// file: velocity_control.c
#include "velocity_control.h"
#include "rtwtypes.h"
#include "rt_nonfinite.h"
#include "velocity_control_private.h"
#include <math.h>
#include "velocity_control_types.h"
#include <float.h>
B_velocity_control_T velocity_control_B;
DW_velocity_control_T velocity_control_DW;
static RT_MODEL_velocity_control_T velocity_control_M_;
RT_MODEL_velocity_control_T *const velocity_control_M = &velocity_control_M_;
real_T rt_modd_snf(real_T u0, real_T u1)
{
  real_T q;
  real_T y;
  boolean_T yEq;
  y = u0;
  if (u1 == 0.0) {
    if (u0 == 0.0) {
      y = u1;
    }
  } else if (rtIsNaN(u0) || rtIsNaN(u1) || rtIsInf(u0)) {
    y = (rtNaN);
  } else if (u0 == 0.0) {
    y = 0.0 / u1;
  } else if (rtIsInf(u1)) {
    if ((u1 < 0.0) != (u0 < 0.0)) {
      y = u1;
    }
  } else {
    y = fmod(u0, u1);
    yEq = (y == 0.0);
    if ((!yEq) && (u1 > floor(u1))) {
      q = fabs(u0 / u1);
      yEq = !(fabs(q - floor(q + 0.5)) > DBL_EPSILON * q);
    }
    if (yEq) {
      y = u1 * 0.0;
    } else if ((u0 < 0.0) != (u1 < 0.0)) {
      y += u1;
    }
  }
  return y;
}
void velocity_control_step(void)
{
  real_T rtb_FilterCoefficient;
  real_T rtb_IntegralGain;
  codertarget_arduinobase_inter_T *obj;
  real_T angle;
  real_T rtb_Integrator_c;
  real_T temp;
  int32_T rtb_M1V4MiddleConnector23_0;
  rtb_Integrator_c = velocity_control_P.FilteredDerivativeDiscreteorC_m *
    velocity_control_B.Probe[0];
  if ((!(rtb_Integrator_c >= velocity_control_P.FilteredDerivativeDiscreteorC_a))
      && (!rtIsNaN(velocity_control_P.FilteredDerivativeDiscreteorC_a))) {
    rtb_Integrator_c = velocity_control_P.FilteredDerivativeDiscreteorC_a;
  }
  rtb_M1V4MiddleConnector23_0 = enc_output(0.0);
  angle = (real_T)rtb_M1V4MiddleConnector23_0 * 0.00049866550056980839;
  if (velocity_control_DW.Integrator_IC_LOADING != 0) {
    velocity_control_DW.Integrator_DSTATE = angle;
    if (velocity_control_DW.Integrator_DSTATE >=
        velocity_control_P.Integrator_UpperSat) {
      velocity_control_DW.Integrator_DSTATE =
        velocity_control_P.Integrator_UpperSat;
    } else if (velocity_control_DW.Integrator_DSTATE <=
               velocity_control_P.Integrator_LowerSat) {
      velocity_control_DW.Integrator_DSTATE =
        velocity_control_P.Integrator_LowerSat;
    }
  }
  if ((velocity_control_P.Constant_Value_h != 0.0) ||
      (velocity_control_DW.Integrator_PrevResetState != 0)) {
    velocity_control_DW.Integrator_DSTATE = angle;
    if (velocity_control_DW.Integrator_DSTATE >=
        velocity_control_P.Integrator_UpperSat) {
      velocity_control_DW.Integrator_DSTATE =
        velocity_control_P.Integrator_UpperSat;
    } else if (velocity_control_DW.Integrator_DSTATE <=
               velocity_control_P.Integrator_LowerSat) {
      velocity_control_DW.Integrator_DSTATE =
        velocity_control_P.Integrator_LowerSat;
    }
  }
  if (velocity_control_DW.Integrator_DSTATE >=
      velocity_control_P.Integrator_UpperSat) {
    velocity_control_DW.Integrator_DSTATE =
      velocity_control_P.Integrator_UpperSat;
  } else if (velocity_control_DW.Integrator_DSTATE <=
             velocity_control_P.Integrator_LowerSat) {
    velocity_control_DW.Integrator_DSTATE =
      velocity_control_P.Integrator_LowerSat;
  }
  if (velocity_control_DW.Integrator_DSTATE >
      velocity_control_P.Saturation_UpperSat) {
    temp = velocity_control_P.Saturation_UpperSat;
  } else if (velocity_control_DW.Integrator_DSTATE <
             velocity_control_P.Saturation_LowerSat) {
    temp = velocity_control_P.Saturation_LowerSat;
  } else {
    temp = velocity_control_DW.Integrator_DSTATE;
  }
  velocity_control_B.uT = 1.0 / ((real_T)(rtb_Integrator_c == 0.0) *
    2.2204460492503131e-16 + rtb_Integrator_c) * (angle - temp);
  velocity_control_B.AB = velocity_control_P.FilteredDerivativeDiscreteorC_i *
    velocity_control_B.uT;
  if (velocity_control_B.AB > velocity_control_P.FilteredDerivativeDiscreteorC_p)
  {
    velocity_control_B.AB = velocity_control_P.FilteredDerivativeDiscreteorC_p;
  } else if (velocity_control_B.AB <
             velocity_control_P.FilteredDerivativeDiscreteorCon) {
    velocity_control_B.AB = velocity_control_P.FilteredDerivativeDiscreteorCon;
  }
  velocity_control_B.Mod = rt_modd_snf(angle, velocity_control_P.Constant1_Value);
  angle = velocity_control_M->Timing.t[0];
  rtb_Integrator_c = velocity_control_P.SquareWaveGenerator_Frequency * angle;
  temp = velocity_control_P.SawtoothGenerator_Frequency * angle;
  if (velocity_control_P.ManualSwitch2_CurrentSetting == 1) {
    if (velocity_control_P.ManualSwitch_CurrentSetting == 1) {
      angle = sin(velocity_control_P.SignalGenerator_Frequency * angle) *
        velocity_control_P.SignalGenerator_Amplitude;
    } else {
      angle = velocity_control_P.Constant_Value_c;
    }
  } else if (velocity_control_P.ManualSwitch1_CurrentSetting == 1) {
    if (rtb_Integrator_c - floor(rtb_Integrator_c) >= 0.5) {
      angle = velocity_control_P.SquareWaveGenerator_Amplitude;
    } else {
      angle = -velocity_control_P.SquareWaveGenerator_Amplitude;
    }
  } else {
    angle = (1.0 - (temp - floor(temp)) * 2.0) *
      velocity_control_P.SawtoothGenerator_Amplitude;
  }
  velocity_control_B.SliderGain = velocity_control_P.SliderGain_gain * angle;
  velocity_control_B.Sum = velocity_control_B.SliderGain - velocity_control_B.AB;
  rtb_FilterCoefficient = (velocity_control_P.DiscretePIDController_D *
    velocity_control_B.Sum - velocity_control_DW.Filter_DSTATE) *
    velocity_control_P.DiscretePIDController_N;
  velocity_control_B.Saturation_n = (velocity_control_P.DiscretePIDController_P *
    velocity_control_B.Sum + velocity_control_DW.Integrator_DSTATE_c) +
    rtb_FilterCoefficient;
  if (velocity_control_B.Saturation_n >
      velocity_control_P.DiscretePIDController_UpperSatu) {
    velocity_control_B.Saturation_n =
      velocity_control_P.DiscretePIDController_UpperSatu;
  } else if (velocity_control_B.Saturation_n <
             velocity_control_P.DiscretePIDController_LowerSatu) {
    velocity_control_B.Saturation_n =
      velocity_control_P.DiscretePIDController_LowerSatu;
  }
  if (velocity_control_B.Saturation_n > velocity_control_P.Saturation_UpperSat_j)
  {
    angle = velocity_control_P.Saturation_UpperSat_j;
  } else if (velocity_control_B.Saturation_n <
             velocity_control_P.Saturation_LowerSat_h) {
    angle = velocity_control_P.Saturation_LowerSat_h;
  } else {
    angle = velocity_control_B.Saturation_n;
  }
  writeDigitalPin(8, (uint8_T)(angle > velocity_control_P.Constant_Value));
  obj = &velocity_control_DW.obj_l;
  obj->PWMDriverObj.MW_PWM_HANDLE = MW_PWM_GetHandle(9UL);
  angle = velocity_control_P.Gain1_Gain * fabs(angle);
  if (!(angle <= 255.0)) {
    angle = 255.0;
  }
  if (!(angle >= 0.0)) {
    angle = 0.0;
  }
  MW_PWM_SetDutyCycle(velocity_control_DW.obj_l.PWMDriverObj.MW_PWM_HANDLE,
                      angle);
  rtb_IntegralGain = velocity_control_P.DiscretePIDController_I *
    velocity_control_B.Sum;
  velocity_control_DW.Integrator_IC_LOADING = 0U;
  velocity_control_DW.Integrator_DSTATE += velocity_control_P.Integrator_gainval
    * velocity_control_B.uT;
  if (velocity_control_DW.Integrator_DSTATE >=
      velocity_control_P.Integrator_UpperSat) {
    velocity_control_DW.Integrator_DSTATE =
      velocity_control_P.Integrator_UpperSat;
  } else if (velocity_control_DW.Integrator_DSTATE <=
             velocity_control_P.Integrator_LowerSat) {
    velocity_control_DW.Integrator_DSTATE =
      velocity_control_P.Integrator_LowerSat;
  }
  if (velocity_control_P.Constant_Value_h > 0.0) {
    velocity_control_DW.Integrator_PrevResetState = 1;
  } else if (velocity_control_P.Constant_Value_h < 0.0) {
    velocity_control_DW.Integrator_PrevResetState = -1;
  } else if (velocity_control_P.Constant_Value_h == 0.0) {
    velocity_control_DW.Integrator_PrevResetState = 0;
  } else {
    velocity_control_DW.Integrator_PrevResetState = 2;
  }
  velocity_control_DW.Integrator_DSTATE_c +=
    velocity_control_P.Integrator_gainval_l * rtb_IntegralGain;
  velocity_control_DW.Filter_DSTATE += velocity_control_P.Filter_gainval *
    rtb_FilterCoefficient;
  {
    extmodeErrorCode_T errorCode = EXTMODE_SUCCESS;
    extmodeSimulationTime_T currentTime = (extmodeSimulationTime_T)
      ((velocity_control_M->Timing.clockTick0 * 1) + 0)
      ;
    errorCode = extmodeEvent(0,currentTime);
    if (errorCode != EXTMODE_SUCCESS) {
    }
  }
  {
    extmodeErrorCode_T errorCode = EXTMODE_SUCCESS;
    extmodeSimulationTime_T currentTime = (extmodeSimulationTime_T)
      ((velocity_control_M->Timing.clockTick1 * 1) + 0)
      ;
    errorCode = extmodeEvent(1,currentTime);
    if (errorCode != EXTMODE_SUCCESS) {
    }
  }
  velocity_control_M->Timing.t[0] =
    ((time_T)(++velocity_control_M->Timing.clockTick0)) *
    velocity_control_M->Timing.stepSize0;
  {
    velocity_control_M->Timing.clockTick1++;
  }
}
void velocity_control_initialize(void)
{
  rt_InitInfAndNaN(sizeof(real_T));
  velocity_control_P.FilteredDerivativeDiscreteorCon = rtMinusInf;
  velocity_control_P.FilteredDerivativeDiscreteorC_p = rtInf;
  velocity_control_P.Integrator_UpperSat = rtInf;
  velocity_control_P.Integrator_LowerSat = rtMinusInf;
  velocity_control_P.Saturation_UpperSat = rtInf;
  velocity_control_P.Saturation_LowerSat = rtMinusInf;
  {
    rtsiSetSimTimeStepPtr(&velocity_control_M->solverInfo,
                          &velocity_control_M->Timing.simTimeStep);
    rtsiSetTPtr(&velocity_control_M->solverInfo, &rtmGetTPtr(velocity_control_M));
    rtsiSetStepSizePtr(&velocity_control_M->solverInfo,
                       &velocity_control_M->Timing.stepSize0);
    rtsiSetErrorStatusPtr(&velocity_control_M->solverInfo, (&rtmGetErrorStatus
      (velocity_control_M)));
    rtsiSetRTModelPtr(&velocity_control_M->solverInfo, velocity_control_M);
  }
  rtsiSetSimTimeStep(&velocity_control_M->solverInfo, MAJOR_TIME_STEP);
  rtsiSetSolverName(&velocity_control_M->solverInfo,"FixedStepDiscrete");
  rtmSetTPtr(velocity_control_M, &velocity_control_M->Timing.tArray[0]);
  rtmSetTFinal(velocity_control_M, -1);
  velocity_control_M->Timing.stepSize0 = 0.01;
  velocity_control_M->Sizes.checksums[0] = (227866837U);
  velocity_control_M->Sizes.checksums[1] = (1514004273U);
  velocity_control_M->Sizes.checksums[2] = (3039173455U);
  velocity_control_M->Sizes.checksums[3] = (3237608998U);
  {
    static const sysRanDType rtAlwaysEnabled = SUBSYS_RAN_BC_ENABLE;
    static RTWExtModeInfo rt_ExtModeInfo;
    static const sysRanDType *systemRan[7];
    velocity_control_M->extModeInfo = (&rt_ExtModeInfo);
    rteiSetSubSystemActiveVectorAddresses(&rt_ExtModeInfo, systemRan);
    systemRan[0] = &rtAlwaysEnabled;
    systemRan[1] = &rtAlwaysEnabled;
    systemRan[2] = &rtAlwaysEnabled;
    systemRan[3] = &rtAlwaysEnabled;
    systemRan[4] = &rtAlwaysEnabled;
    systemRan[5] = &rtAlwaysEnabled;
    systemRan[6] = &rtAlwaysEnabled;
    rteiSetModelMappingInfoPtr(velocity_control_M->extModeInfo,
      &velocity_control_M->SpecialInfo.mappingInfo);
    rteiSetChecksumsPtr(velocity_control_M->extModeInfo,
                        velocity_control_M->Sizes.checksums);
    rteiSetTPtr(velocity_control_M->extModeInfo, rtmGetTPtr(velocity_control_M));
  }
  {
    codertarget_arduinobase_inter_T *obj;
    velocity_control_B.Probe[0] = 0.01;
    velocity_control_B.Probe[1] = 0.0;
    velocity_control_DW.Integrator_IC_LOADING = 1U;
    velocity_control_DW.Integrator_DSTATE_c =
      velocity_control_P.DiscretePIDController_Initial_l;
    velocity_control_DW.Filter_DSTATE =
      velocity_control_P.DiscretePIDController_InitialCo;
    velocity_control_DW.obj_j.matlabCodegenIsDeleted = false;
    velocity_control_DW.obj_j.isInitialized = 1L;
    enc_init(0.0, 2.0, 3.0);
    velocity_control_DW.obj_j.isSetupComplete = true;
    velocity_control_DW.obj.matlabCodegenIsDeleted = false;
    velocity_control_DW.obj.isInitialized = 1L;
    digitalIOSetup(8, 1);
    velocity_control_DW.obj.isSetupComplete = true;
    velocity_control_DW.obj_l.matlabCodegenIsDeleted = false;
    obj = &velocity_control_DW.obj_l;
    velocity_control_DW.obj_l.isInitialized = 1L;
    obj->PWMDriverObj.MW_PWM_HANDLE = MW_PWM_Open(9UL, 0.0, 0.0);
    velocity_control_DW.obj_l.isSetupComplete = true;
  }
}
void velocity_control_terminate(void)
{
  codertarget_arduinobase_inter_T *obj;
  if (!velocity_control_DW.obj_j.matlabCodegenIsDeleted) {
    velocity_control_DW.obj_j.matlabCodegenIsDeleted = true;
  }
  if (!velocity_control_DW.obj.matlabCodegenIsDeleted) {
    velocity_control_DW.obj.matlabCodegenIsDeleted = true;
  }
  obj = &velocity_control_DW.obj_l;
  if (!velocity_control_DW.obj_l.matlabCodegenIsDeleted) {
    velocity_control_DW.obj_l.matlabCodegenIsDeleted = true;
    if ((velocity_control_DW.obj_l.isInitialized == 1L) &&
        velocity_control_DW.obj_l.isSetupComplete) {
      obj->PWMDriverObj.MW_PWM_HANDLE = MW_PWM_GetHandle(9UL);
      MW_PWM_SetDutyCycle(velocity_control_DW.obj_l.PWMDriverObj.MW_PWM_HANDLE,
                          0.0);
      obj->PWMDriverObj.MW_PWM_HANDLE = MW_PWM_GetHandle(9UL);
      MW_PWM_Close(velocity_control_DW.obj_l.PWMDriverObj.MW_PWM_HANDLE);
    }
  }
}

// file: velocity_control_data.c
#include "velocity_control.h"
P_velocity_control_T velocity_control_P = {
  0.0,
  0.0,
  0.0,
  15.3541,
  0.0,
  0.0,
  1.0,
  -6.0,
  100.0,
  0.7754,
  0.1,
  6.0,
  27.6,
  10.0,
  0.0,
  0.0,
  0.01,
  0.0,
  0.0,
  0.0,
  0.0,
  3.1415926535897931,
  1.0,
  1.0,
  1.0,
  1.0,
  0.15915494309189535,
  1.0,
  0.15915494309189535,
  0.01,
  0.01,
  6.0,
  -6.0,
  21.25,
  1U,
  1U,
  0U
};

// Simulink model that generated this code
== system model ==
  Mod : Math  Operator=mod  <- 1: MATLABFunction#1, 2: Constant1
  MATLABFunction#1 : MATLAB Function  <- 1: DataTypeConversion#1
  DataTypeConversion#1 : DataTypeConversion  <- 1: M1V4MiddleConnector23
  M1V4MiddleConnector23 : MinSegLibrary_M1V4/M1V4 Middle Connector 2,3
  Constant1 : Constant  Value=pi
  DigitalOutput#1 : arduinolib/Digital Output  pinNumber=8  <- 1: CompareToZero#1
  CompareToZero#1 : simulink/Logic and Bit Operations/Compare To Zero  relop=>  <- 1: Saturation
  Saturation : Saturate  UpperLimit=6  LowerLimit=-6  <- 1: DiscretePIDController
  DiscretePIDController : slpidlib/PID Controller  Controller=PID  Form=Parallel  TimeDomain=Discrete-time  IntegratorMethod=Forward Euler  P=0.7754  I=15.3541  D=0  N=100  InitialConditionForIntegrator=0  ExternalReset=none  LimitOutput=on  UpperSaturationLimit=6  LowerSaturationLimit=-6  <- 1: Sum
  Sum : Sum  Inputs=+-  <- 1: SliderGain, 2: FilteredDerivativeDiscreteorContinuous#1
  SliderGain : simulink/Math Operations/Slider Gain  <- 1: ManualSwitch2
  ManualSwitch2 : ManualSwitch  <- 1: ManualSwitch, 2: ManualSwitch1
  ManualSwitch : ManualSwitch  <- 1: SignalGenerator, 2: Constant
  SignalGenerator : SignalGenerator
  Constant : Constant
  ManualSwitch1 : ManualSwitch  <- 1: SquareWaveGenerator, 2: SawtoothGenerator
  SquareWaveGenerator : SignalGenerator
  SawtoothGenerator : SignalGenerator
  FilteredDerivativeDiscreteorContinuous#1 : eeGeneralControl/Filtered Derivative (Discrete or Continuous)  B=inf  A=-inf  <- 1: MATLABFunction#1
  PWM : arduinolib/PWM  pinNumber=9  <- 1: Gain1
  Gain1 : Gain  Gain=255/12  <- 1: Abs#1
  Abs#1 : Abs  <- 1: Saturation
== matlab function MATLABFunction#1 ==
function angle = count2angle(u)

N = 500; Q = 4; G = 6.3;
factor = 2 * pi / (N*Q*G);
angle = u * factor;
